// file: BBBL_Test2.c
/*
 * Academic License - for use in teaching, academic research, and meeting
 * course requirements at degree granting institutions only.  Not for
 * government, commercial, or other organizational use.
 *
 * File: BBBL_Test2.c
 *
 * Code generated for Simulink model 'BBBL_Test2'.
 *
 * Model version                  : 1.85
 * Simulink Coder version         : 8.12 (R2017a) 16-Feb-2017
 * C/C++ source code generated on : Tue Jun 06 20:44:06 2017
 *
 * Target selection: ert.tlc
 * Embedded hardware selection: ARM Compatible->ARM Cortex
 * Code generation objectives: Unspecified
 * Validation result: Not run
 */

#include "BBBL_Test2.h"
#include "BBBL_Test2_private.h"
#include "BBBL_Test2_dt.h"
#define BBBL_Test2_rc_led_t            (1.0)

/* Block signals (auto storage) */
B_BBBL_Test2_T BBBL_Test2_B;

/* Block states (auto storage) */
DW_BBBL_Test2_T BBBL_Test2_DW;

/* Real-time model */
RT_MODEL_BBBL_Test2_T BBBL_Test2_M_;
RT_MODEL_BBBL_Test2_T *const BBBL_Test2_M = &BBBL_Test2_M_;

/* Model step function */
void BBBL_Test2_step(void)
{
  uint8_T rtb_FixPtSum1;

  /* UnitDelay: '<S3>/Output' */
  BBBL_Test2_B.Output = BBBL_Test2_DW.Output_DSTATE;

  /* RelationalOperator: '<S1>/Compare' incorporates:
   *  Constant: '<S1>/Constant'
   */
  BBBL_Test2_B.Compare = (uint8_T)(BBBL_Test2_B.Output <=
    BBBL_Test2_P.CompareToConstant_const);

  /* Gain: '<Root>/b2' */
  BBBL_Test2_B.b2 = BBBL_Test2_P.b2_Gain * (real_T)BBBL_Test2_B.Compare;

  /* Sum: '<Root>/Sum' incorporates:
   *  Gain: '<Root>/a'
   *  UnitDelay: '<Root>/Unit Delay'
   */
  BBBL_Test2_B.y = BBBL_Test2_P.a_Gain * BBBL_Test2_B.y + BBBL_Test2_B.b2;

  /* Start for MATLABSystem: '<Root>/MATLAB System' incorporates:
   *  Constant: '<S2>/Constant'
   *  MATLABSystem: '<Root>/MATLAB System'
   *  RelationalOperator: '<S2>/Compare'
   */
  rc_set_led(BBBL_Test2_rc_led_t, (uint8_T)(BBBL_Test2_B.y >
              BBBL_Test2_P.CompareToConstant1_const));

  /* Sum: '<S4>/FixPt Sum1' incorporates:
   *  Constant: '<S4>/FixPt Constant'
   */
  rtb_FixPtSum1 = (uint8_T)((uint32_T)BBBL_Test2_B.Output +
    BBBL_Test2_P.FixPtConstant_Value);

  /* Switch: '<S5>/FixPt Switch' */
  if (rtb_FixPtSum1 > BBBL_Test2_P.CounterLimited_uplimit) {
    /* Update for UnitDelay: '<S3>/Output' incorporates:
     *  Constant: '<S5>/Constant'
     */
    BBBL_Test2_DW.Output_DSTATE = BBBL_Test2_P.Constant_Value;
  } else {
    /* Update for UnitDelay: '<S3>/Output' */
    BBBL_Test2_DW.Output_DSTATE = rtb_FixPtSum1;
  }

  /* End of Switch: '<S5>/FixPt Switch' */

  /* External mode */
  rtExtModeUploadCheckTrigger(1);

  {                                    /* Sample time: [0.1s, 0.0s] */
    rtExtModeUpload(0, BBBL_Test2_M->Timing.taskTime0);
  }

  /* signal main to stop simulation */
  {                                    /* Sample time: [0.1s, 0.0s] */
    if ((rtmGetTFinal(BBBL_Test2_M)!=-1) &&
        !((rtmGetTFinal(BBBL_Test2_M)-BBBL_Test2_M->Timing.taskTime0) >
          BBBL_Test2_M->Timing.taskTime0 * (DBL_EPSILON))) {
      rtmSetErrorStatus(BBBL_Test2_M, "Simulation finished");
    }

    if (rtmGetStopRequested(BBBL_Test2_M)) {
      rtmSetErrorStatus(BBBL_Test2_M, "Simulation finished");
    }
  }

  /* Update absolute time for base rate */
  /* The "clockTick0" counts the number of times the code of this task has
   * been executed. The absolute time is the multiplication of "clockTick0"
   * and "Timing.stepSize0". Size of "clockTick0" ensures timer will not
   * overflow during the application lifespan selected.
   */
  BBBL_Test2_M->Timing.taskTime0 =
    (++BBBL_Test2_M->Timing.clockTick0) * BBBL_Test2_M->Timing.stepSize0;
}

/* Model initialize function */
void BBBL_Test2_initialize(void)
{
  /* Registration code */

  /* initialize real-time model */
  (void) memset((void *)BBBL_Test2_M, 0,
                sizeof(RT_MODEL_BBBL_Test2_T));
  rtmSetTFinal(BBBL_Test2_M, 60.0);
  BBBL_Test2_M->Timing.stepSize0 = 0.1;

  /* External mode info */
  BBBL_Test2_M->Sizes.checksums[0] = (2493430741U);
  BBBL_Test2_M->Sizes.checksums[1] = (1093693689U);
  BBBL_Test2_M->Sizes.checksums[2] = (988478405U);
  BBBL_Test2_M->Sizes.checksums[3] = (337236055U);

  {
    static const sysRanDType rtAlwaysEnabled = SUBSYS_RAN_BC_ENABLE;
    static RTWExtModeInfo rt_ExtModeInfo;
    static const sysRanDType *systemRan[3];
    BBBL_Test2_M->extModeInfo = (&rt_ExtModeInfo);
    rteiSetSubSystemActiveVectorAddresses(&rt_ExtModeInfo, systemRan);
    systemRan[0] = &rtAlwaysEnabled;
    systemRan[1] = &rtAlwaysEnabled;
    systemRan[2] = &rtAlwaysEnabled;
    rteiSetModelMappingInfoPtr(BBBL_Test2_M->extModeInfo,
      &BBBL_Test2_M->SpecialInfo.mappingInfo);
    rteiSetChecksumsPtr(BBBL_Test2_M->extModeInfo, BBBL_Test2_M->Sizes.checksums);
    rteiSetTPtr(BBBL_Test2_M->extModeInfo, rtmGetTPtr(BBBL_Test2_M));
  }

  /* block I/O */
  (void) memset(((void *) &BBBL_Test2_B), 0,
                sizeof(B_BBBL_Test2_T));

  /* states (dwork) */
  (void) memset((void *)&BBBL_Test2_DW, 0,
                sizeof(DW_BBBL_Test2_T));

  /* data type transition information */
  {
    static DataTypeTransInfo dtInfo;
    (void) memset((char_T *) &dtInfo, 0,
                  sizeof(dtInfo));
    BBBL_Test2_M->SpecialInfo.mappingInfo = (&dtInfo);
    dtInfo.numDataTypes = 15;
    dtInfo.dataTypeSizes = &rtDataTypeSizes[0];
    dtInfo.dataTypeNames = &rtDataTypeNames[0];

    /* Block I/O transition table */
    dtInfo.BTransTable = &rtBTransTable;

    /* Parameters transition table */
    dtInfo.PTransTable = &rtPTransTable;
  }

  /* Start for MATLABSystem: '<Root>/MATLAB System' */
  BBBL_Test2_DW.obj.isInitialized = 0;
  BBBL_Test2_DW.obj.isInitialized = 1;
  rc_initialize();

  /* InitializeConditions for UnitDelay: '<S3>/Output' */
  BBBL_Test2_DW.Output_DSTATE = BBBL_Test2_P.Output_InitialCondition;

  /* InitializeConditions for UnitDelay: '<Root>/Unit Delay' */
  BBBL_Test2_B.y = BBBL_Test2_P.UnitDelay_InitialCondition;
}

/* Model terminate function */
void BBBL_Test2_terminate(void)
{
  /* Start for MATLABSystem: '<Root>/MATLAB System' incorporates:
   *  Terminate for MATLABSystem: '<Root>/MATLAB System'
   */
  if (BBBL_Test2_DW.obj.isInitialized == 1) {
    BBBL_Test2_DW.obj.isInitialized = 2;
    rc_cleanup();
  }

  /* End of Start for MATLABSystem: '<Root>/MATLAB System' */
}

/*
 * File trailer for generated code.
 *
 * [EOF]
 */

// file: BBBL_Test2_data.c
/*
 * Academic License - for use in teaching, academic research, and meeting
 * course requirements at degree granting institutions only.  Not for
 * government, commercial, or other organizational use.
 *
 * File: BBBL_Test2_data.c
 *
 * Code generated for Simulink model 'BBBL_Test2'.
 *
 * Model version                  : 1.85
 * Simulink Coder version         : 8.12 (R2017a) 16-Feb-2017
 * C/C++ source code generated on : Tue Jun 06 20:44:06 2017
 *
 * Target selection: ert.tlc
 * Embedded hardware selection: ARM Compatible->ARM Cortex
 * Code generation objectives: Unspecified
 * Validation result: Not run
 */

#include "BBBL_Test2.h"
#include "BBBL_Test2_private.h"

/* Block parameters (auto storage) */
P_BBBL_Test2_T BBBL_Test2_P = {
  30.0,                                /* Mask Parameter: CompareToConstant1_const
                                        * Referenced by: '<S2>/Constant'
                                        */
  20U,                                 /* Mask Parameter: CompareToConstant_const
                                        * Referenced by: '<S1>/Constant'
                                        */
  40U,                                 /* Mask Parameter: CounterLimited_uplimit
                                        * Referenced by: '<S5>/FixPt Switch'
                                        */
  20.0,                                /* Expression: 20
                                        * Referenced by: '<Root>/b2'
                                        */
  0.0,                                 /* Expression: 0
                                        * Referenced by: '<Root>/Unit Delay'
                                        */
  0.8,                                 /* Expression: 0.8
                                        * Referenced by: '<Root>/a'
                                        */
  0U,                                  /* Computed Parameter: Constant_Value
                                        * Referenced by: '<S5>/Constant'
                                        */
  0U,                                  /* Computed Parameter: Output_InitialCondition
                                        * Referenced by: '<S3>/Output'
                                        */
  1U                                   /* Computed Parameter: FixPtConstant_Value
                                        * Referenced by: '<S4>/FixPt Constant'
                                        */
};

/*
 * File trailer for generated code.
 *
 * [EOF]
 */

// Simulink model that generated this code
simulink model "BBBL_Test2"  (R2017a)
settings: Solver=FixedStepDiscrete  StartTime=0.0  StopTime=60.0  RelTol=1e-3  EnableMultiTasking=on
libraries: simulink x3

== system BBBL_Test2 ==
  note: Copyright 2017, The MathWorks, Inc.
  <=20 : Scope
  Compare To Constant : simulink/Logic and Bit Operations/Compare To Constant  relop=<=  const=20  OutDataTypeStr=uint8
  Compare To Constant1 : simulink/Logic and Bit Operations/Compare To Constant  relop=>  const=30.0  OutDataTypeStr=uint8
  Counter : Scope
  Counter Limited : simulink/Sources/Counter Limited  uplimit=40  tsamp=0.1
  Input : Scope
  MATLAB System : MATLABSystem  System=rc_blink_sys  rc_led_t=1
  Output : Scope
  Sum : Sum  Inputs=|++
  Unit Delay : UnitDelay  SampleTime=-1
  a : Gain  Gain=0.8  SaturateOnIntegerOverflow=on  OutDataTypeStr=Inherit: Same as input  ParamDataTypeStr=Inherit: Same as input
  b2 : Gain  Gain=20  ParamDataTypeStr=double  OutDataTypeStr=double  SaturateOnIntegerOverflow=on
  wires:
  a/1 -> Sum/2
  Unit Delay/1 -> a/1
  Sum/1 -> Unit Delay/1, Output/1, Compare To Constant1/1  "y"
  Counter Limited/1 -> Counter/1, Compare To Constant/1
  Compare To Constant/1 -> <=20/1, b2/1
  b2/1 -> Input/1, Sum/1
  Compare To Constant1/1 -> MATLAB System/1
